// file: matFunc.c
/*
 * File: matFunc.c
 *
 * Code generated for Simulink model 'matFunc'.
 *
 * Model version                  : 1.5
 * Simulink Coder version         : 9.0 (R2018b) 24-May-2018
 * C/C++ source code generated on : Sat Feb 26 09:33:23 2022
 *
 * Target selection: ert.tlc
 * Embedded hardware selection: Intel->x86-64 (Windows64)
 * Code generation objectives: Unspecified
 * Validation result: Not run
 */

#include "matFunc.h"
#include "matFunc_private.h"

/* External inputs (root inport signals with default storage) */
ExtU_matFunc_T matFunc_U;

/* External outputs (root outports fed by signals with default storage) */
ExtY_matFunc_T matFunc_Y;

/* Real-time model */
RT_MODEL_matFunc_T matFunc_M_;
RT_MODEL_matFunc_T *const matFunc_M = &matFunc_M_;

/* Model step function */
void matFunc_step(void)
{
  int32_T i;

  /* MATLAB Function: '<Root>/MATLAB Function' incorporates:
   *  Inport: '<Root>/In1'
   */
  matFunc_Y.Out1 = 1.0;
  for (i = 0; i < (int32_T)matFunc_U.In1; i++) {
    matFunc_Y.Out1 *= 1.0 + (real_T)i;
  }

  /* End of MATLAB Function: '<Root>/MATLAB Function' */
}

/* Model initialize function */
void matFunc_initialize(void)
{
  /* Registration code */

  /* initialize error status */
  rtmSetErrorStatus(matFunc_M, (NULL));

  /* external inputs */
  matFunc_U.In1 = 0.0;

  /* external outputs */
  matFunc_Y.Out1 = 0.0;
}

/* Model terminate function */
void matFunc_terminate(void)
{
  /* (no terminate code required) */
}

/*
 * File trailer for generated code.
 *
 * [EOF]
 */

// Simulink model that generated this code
simulink model "matFunc"  (R2018b)
settings: Solver=FixedStepDiscrete  StartTime=0.0  StopTime=10.0  RelTol=1e-3

== system matFunc ==
  In1 : Inport
  Display : Display
  MATLAB Function : MATLAB Function  TreatAsAtomicUnit=on
  Out1 : Outport
  wires:
  In1/1 -> MATLAB Function/1(u)
  MATLAB Function/1(y) -> Display/1, Out1/1

== matlab function matFunc/MATLAB Function ==
function y = fcn(u)
    y=1;
    for i = 1:u %looping through values from 1 : n to multiply each value;
        y = y*i; %multiplying with our previous values.
    end
end
